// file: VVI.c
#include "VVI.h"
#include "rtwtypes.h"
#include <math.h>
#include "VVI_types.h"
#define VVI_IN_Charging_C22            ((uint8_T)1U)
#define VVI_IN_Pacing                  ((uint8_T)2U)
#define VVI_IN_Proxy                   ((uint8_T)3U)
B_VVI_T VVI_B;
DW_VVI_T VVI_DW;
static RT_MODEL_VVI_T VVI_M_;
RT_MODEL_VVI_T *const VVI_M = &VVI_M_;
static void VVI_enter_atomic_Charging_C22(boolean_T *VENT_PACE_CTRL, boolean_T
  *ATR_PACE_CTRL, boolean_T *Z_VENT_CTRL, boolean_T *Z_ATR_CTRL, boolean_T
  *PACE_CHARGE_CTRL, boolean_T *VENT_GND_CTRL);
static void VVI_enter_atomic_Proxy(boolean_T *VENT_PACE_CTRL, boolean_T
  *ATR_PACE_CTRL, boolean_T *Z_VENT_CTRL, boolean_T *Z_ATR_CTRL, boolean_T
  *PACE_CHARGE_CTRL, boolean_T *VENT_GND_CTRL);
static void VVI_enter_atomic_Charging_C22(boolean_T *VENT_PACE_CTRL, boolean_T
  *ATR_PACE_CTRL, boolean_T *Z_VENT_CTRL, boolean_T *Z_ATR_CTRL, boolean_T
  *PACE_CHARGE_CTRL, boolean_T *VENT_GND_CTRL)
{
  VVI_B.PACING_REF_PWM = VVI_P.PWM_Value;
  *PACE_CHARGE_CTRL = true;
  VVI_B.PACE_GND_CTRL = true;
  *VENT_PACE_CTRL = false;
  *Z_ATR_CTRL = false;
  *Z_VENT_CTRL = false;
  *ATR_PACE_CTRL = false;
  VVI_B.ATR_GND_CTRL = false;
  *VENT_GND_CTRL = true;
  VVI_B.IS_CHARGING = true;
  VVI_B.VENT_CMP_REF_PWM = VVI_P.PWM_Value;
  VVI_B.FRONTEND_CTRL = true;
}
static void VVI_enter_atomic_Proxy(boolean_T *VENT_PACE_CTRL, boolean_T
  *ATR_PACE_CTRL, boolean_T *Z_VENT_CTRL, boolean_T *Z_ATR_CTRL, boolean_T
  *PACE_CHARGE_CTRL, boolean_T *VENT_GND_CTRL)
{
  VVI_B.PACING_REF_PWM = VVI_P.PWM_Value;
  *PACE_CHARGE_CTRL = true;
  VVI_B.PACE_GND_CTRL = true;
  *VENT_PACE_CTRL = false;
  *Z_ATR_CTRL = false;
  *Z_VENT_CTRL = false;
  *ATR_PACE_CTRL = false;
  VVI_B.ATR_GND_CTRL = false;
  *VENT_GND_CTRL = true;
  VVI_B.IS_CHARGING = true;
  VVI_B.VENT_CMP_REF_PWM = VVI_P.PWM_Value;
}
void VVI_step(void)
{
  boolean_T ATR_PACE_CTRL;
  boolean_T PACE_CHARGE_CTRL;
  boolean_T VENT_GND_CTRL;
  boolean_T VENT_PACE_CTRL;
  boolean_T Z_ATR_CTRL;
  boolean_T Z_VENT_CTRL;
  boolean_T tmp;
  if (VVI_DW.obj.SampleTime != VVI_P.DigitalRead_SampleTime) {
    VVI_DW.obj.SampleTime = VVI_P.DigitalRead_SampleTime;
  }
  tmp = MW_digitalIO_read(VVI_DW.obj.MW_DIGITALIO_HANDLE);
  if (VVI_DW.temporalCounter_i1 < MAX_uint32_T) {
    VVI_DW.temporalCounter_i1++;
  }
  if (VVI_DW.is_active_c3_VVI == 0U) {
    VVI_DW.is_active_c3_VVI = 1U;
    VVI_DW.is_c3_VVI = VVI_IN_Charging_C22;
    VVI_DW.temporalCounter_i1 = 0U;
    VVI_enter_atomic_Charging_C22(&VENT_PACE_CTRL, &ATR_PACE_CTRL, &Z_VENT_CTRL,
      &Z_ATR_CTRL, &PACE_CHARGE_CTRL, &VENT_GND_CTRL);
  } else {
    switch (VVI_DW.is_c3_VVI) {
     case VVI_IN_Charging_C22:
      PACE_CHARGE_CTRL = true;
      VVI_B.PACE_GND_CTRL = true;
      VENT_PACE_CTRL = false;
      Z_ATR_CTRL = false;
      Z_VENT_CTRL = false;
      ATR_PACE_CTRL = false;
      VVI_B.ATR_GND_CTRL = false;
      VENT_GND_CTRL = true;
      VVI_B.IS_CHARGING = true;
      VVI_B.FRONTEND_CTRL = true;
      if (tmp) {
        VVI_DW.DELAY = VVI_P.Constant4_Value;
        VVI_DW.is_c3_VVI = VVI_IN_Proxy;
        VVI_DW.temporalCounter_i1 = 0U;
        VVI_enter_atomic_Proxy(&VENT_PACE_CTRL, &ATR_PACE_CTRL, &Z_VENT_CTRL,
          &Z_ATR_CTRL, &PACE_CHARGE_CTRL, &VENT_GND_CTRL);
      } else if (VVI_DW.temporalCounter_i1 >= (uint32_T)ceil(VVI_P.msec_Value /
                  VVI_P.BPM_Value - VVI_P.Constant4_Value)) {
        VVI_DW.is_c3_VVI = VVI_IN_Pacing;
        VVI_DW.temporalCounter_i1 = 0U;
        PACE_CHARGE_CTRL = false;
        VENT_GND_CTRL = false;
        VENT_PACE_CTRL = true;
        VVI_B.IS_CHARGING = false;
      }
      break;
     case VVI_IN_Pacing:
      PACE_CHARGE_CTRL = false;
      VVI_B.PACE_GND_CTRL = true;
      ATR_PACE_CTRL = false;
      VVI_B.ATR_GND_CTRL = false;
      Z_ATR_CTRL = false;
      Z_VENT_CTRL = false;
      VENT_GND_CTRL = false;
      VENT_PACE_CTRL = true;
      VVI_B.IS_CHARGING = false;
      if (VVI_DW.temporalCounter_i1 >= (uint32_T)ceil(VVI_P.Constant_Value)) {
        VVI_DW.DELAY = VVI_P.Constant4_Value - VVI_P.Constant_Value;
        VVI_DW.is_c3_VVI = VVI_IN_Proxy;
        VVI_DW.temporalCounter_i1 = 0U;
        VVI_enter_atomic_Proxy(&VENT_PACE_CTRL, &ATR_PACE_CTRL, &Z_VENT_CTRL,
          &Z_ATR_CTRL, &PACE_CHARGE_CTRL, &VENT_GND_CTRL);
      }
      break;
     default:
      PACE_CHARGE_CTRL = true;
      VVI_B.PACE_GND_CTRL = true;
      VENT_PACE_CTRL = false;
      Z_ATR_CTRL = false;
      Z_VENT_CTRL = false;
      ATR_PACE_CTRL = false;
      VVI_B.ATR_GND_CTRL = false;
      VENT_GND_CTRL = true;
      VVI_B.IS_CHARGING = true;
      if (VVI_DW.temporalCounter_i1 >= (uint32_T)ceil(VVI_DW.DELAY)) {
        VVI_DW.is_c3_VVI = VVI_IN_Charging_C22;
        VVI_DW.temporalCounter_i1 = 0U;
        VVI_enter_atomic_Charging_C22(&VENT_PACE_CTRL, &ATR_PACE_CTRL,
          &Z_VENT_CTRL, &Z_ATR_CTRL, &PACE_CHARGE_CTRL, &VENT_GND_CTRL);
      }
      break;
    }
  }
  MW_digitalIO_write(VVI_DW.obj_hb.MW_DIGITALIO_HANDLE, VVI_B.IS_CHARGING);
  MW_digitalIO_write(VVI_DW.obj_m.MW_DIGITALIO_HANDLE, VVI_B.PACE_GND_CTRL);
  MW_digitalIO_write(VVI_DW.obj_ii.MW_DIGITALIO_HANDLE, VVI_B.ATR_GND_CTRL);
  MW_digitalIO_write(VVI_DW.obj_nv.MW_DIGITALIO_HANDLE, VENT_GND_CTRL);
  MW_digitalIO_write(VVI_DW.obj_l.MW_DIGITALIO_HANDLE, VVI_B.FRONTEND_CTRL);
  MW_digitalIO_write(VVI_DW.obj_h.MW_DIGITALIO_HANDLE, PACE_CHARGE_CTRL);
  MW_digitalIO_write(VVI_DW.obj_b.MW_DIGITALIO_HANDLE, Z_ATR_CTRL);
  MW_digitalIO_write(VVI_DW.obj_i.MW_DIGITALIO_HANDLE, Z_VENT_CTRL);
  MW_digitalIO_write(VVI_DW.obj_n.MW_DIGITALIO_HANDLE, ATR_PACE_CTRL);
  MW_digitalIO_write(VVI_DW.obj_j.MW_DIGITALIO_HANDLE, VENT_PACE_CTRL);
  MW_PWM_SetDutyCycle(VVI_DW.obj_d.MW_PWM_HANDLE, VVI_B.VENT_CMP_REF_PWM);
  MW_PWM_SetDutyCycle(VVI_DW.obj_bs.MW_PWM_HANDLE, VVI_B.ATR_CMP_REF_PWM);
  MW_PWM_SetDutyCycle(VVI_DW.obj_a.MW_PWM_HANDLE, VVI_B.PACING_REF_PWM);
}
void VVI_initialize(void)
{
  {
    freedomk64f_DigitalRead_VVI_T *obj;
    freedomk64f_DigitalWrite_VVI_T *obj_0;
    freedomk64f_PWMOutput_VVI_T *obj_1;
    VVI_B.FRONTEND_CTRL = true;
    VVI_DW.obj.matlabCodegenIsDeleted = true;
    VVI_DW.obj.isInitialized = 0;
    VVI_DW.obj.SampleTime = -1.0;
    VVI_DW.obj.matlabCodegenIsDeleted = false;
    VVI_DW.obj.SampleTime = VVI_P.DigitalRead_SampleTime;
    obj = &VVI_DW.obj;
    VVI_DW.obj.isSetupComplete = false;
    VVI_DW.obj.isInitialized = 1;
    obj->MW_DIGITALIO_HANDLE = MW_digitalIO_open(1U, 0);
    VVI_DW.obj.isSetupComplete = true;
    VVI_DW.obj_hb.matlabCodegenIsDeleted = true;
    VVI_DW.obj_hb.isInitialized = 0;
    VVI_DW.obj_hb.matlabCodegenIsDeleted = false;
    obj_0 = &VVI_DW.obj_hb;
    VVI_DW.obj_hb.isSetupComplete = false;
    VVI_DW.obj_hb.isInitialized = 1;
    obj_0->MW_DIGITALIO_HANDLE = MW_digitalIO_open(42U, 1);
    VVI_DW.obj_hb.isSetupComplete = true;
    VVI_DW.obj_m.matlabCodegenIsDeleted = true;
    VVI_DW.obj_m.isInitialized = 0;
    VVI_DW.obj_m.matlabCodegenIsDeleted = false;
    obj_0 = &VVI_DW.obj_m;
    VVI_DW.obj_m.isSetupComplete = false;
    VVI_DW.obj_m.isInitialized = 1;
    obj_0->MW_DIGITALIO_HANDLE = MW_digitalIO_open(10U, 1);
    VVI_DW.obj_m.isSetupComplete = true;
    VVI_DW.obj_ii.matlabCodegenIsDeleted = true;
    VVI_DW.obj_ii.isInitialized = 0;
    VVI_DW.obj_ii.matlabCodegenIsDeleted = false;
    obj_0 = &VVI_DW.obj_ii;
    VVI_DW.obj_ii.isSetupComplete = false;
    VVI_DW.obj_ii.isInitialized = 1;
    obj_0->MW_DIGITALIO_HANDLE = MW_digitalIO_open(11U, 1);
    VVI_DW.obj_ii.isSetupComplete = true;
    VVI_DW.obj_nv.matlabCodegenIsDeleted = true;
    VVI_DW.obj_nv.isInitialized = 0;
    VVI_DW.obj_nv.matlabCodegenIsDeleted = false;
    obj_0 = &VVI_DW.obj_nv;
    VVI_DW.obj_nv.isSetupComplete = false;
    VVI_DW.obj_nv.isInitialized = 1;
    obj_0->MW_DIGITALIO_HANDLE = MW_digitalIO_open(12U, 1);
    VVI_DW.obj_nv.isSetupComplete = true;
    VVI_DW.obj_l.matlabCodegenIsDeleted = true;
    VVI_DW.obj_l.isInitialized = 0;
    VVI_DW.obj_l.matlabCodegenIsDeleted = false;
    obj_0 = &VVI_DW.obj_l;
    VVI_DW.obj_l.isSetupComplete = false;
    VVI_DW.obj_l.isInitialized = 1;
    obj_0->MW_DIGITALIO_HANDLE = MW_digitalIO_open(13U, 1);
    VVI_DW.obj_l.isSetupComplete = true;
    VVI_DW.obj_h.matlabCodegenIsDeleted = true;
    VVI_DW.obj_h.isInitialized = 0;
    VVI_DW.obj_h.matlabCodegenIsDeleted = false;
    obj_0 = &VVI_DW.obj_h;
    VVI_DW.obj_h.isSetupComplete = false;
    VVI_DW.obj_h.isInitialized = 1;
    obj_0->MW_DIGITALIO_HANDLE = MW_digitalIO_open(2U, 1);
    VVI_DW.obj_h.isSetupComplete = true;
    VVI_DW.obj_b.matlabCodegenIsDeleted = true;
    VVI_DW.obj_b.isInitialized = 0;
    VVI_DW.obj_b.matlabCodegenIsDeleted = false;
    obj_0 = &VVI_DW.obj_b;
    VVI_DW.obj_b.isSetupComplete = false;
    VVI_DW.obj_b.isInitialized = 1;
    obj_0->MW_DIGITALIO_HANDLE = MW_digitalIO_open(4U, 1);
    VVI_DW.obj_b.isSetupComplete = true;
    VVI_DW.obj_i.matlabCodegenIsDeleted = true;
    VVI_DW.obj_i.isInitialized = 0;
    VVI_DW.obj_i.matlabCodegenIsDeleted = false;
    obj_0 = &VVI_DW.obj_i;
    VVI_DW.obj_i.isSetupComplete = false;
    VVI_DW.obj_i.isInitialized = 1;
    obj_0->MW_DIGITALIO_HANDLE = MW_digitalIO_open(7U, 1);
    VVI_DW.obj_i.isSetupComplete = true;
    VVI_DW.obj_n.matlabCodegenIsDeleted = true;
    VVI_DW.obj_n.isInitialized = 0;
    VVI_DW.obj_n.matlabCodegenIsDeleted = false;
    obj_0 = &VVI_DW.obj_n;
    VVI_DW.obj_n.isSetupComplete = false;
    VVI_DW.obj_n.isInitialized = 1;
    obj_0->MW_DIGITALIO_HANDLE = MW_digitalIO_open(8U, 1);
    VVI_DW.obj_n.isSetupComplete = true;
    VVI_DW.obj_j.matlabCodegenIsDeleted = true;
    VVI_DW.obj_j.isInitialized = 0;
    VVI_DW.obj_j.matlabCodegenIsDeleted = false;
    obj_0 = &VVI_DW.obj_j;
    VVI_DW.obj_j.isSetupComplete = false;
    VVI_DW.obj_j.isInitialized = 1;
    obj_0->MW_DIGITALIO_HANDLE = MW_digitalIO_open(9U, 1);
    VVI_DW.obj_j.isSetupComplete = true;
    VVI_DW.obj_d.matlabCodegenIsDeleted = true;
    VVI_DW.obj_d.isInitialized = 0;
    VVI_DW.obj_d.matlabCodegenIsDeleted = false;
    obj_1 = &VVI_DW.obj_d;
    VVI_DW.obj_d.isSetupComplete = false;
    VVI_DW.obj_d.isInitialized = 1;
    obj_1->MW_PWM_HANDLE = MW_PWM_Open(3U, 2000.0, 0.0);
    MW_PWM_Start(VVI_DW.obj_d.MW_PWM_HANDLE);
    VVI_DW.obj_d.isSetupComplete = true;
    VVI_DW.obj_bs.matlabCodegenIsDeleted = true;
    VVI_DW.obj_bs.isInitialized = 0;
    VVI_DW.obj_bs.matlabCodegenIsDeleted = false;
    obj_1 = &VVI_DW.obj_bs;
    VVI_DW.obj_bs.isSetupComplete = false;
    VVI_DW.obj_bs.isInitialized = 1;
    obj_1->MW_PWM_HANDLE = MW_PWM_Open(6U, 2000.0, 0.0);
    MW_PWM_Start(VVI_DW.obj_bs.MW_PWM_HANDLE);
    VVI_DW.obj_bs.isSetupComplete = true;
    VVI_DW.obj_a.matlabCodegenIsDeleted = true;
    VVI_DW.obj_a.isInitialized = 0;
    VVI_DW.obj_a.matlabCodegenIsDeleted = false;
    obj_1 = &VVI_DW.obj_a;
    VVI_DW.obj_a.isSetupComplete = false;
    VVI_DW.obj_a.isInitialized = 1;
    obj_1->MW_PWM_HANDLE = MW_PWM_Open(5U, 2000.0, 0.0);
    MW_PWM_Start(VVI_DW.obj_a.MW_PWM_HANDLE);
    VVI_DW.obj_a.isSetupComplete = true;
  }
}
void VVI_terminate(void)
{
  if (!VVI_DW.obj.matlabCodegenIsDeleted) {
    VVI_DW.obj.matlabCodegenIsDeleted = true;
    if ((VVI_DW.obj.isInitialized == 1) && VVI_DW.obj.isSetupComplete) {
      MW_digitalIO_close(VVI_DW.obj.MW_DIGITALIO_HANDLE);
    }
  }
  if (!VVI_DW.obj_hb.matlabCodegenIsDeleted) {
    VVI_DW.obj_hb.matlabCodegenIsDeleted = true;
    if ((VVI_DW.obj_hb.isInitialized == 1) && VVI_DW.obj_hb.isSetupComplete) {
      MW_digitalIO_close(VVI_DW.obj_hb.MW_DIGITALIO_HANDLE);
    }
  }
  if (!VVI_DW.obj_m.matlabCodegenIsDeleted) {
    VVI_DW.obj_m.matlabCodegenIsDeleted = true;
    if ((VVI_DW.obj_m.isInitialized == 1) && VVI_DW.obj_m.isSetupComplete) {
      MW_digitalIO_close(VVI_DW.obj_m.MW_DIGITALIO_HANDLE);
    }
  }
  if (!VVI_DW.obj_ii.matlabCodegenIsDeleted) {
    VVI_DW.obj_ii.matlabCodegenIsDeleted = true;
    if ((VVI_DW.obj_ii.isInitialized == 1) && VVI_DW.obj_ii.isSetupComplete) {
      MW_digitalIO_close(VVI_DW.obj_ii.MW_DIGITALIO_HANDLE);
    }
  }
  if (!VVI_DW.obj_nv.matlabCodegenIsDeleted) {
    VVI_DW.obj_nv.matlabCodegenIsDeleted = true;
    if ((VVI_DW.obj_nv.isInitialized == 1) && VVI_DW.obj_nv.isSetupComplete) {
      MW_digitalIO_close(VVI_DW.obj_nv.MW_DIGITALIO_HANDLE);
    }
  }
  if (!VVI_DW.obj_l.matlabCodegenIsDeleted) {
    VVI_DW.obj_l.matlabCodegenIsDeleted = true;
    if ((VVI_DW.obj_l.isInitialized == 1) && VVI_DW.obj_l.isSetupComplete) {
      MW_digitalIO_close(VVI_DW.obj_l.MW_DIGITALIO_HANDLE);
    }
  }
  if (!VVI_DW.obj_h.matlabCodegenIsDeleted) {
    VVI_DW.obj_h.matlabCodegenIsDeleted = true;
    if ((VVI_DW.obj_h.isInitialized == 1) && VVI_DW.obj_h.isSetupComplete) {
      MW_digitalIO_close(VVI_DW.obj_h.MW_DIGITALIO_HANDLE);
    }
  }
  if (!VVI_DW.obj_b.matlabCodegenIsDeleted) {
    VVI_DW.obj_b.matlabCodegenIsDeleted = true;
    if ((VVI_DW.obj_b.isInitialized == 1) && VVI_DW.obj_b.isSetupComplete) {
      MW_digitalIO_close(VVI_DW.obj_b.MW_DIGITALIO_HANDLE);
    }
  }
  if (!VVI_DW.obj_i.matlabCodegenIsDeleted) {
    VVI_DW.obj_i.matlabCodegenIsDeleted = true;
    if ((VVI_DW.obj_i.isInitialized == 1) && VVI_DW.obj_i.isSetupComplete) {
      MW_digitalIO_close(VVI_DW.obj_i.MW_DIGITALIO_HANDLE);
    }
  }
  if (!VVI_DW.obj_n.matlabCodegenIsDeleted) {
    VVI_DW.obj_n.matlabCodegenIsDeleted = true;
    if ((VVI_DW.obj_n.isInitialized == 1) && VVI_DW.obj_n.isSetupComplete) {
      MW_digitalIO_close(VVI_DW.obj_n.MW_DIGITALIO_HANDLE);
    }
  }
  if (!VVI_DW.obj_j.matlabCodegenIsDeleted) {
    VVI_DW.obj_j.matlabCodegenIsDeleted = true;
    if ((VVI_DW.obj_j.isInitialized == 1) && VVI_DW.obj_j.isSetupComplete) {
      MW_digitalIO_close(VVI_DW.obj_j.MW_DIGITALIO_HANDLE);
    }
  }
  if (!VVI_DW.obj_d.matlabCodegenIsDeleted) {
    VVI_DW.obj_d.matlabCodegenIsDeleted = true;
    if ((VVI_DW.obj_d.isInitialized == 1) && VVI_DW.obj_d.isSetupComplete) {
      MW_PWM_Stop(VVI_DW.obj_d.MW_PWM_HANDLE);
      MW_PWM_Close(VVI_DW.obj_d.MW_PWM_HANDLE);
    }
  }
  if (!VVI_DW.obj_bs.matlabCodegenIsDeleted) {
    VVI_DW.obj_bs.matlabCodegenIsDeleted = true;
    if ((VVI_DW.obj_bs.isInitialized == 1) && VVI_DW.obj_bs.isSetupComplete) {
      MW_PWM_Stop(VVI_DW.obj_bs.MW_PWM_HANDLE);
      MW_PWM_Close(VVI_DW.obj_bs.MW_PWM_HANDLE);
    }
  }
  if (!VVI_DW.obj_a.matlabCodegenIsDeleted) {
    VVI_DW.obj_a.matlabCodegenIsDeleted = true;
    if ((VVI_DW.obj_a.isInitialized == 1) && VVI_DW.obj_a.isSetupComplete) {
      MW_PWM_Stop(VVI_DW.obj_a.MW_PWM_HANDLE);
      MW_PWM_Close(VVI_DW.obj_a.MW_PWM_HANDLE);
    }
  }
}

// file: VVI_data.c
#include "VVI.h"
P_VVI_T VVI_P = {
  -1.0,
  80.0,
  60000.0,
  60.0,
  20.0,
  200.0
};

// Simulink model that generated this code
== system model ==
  DigitalWrite : frdmk64flib/Digital Write  <- 1: Stateflowchart#1
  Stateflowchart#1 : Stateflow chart  <- 1: PWM, 2: Product#1, 3: Constant, 4: DigitalRead, 5: Constant4
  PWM : Constant  Value=80
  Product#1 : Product  Inputs=*/  <- 1: msec, 2: BPM
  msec : Constant  Value=60000
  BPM : Constant  Value=60
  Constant : Constant  Value=20
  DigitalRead : frdmk64flib/Digital Read
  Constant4 : Constant  Value=200
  DigitalWrite#1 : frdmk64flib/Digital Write  <- 1: Stateflowchart#1/10
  DigitalWrite#2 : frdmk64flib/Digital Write  <- 1: Stateflowchart#1/11
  DigitalWrite#3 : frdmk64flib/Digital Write  <- 1: Stateflowchart#1/12
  DigitalWrite#4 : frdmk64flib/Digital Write  <- 1: Stateflowchart#1/13
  DigitalWrite#5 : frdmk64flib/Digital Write  <- 1: Stateflowchart#1/2
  DigitalWrite#6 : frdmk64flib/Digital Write  <- 1: Stateflowchart#1/4
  DigitalWrite#7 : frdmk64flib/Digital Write  <- 1: Stateflowchart#1/7
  DigitalWrite#8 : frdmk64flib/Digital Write  <- 1: Stateflowchart#1/8
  DigitalWrite#9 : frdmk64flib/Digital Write  <- 1: Stateflowchart#1/9
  PWMOutput : frdmk64flib/PWM Output  <- 1: Stateflowchart#1/3
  PWMOutput#1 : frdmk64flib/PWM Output  <- 1: Stateflowchart#1/6
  PWMOutput#2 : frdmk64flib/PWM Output  <- 1: Stateflowchart#1/5
== stateflow chart Stateflowchart#1 ==
  state Charging_C22
    entry:
    PACING_REF_PWM = DUTY_CYCLE
    PACE_CHARGE_CTRL = true
    PACE_GND_CTRL = true
    VENT_PACE_CTRL = false
    Z_ATR_CTRL = false
    Z_VENT_CTRL = false
    ATR_PACE_CTRL = false
    ATR_GND_CTRL = false
    VENT_GND_CTRL = true
    % For LED testing
    IS_CHARGING = true
    VENT_CMP_REF_PWM = DUTY_CYCLE
    FRONTEND_CTRL = true
  state Proxy
    entry:
    PACING_REF_PWM = DUTY_CYCLE
    PACE_CHARGE_CTRL = true
    PACE_GND_CTRL = true
    VENT_PACE_CTRL = false
    Z_ATR_CTRL = false
    Z_VENT_CTRL = false
    ATR_PACE_CTRL = false
    ATR_GND_CTRL = false
    VENT_GND_CTRL = true
    % For LED testing
    IS_CHARGING = true
    VENT_CMP_REF_PWM = DUTY_CYCLE
  state Pacing
    entry:
    PACE_CHARGE_CTRL = false
    PACE_GND_CTRL = true
    ATR_PACE_CTRL = false
    ATR_GND_CTRL = false
    Z_ATR_CTRL = false
    Z_VENT_CTRL = false
    VENT_GND_CTRL = false
    VENT_PACE_CTRL = true
    % For LED testing
    IS_CHARGING = false
  (default) -> Charging_C22
  Charging_C22 -> Proxy [order 1] : [VENT_CMP_DETECT ==  true]{DELAY = REFRACTORY_PERIOD}
  Proxy -> Charging_C22 : [after(DELAY,msec)]
  Charging_C22 -> Pacing [order 2] : [after(PULSE_PERIOD-REFRACTORY_PERIOD,msec)]
  Pacing -> Proxy : [after(PULSE_WIDTH,msec)]{DELAY = REFRACTORY_PERIOD - PULSE_WIDTH }
  data: IS_CHARGING output; PACE_CHARGE_CTRL output; VENT_CMP_REF_PWM output =0; Z_ATR_CTRL output; PACING_REF_PWM output; ATR_CMP_REF_PWM output =0; Z_VENT_CTRL output; ATR_PACE_CTRL output; VENT_PACE_CTRL output; PACE_GND_CTRL output; ATR_GND_CTRL output; VENT_GND_CTRL output; FRONTEND_CTRL output =true; DUTY_CYCLE input; PULSE_PERIOD input; PULSE_WIDTH input; VENT_CMP_DETECT input; DELAY local; REFRACTORY_PERIOD input
